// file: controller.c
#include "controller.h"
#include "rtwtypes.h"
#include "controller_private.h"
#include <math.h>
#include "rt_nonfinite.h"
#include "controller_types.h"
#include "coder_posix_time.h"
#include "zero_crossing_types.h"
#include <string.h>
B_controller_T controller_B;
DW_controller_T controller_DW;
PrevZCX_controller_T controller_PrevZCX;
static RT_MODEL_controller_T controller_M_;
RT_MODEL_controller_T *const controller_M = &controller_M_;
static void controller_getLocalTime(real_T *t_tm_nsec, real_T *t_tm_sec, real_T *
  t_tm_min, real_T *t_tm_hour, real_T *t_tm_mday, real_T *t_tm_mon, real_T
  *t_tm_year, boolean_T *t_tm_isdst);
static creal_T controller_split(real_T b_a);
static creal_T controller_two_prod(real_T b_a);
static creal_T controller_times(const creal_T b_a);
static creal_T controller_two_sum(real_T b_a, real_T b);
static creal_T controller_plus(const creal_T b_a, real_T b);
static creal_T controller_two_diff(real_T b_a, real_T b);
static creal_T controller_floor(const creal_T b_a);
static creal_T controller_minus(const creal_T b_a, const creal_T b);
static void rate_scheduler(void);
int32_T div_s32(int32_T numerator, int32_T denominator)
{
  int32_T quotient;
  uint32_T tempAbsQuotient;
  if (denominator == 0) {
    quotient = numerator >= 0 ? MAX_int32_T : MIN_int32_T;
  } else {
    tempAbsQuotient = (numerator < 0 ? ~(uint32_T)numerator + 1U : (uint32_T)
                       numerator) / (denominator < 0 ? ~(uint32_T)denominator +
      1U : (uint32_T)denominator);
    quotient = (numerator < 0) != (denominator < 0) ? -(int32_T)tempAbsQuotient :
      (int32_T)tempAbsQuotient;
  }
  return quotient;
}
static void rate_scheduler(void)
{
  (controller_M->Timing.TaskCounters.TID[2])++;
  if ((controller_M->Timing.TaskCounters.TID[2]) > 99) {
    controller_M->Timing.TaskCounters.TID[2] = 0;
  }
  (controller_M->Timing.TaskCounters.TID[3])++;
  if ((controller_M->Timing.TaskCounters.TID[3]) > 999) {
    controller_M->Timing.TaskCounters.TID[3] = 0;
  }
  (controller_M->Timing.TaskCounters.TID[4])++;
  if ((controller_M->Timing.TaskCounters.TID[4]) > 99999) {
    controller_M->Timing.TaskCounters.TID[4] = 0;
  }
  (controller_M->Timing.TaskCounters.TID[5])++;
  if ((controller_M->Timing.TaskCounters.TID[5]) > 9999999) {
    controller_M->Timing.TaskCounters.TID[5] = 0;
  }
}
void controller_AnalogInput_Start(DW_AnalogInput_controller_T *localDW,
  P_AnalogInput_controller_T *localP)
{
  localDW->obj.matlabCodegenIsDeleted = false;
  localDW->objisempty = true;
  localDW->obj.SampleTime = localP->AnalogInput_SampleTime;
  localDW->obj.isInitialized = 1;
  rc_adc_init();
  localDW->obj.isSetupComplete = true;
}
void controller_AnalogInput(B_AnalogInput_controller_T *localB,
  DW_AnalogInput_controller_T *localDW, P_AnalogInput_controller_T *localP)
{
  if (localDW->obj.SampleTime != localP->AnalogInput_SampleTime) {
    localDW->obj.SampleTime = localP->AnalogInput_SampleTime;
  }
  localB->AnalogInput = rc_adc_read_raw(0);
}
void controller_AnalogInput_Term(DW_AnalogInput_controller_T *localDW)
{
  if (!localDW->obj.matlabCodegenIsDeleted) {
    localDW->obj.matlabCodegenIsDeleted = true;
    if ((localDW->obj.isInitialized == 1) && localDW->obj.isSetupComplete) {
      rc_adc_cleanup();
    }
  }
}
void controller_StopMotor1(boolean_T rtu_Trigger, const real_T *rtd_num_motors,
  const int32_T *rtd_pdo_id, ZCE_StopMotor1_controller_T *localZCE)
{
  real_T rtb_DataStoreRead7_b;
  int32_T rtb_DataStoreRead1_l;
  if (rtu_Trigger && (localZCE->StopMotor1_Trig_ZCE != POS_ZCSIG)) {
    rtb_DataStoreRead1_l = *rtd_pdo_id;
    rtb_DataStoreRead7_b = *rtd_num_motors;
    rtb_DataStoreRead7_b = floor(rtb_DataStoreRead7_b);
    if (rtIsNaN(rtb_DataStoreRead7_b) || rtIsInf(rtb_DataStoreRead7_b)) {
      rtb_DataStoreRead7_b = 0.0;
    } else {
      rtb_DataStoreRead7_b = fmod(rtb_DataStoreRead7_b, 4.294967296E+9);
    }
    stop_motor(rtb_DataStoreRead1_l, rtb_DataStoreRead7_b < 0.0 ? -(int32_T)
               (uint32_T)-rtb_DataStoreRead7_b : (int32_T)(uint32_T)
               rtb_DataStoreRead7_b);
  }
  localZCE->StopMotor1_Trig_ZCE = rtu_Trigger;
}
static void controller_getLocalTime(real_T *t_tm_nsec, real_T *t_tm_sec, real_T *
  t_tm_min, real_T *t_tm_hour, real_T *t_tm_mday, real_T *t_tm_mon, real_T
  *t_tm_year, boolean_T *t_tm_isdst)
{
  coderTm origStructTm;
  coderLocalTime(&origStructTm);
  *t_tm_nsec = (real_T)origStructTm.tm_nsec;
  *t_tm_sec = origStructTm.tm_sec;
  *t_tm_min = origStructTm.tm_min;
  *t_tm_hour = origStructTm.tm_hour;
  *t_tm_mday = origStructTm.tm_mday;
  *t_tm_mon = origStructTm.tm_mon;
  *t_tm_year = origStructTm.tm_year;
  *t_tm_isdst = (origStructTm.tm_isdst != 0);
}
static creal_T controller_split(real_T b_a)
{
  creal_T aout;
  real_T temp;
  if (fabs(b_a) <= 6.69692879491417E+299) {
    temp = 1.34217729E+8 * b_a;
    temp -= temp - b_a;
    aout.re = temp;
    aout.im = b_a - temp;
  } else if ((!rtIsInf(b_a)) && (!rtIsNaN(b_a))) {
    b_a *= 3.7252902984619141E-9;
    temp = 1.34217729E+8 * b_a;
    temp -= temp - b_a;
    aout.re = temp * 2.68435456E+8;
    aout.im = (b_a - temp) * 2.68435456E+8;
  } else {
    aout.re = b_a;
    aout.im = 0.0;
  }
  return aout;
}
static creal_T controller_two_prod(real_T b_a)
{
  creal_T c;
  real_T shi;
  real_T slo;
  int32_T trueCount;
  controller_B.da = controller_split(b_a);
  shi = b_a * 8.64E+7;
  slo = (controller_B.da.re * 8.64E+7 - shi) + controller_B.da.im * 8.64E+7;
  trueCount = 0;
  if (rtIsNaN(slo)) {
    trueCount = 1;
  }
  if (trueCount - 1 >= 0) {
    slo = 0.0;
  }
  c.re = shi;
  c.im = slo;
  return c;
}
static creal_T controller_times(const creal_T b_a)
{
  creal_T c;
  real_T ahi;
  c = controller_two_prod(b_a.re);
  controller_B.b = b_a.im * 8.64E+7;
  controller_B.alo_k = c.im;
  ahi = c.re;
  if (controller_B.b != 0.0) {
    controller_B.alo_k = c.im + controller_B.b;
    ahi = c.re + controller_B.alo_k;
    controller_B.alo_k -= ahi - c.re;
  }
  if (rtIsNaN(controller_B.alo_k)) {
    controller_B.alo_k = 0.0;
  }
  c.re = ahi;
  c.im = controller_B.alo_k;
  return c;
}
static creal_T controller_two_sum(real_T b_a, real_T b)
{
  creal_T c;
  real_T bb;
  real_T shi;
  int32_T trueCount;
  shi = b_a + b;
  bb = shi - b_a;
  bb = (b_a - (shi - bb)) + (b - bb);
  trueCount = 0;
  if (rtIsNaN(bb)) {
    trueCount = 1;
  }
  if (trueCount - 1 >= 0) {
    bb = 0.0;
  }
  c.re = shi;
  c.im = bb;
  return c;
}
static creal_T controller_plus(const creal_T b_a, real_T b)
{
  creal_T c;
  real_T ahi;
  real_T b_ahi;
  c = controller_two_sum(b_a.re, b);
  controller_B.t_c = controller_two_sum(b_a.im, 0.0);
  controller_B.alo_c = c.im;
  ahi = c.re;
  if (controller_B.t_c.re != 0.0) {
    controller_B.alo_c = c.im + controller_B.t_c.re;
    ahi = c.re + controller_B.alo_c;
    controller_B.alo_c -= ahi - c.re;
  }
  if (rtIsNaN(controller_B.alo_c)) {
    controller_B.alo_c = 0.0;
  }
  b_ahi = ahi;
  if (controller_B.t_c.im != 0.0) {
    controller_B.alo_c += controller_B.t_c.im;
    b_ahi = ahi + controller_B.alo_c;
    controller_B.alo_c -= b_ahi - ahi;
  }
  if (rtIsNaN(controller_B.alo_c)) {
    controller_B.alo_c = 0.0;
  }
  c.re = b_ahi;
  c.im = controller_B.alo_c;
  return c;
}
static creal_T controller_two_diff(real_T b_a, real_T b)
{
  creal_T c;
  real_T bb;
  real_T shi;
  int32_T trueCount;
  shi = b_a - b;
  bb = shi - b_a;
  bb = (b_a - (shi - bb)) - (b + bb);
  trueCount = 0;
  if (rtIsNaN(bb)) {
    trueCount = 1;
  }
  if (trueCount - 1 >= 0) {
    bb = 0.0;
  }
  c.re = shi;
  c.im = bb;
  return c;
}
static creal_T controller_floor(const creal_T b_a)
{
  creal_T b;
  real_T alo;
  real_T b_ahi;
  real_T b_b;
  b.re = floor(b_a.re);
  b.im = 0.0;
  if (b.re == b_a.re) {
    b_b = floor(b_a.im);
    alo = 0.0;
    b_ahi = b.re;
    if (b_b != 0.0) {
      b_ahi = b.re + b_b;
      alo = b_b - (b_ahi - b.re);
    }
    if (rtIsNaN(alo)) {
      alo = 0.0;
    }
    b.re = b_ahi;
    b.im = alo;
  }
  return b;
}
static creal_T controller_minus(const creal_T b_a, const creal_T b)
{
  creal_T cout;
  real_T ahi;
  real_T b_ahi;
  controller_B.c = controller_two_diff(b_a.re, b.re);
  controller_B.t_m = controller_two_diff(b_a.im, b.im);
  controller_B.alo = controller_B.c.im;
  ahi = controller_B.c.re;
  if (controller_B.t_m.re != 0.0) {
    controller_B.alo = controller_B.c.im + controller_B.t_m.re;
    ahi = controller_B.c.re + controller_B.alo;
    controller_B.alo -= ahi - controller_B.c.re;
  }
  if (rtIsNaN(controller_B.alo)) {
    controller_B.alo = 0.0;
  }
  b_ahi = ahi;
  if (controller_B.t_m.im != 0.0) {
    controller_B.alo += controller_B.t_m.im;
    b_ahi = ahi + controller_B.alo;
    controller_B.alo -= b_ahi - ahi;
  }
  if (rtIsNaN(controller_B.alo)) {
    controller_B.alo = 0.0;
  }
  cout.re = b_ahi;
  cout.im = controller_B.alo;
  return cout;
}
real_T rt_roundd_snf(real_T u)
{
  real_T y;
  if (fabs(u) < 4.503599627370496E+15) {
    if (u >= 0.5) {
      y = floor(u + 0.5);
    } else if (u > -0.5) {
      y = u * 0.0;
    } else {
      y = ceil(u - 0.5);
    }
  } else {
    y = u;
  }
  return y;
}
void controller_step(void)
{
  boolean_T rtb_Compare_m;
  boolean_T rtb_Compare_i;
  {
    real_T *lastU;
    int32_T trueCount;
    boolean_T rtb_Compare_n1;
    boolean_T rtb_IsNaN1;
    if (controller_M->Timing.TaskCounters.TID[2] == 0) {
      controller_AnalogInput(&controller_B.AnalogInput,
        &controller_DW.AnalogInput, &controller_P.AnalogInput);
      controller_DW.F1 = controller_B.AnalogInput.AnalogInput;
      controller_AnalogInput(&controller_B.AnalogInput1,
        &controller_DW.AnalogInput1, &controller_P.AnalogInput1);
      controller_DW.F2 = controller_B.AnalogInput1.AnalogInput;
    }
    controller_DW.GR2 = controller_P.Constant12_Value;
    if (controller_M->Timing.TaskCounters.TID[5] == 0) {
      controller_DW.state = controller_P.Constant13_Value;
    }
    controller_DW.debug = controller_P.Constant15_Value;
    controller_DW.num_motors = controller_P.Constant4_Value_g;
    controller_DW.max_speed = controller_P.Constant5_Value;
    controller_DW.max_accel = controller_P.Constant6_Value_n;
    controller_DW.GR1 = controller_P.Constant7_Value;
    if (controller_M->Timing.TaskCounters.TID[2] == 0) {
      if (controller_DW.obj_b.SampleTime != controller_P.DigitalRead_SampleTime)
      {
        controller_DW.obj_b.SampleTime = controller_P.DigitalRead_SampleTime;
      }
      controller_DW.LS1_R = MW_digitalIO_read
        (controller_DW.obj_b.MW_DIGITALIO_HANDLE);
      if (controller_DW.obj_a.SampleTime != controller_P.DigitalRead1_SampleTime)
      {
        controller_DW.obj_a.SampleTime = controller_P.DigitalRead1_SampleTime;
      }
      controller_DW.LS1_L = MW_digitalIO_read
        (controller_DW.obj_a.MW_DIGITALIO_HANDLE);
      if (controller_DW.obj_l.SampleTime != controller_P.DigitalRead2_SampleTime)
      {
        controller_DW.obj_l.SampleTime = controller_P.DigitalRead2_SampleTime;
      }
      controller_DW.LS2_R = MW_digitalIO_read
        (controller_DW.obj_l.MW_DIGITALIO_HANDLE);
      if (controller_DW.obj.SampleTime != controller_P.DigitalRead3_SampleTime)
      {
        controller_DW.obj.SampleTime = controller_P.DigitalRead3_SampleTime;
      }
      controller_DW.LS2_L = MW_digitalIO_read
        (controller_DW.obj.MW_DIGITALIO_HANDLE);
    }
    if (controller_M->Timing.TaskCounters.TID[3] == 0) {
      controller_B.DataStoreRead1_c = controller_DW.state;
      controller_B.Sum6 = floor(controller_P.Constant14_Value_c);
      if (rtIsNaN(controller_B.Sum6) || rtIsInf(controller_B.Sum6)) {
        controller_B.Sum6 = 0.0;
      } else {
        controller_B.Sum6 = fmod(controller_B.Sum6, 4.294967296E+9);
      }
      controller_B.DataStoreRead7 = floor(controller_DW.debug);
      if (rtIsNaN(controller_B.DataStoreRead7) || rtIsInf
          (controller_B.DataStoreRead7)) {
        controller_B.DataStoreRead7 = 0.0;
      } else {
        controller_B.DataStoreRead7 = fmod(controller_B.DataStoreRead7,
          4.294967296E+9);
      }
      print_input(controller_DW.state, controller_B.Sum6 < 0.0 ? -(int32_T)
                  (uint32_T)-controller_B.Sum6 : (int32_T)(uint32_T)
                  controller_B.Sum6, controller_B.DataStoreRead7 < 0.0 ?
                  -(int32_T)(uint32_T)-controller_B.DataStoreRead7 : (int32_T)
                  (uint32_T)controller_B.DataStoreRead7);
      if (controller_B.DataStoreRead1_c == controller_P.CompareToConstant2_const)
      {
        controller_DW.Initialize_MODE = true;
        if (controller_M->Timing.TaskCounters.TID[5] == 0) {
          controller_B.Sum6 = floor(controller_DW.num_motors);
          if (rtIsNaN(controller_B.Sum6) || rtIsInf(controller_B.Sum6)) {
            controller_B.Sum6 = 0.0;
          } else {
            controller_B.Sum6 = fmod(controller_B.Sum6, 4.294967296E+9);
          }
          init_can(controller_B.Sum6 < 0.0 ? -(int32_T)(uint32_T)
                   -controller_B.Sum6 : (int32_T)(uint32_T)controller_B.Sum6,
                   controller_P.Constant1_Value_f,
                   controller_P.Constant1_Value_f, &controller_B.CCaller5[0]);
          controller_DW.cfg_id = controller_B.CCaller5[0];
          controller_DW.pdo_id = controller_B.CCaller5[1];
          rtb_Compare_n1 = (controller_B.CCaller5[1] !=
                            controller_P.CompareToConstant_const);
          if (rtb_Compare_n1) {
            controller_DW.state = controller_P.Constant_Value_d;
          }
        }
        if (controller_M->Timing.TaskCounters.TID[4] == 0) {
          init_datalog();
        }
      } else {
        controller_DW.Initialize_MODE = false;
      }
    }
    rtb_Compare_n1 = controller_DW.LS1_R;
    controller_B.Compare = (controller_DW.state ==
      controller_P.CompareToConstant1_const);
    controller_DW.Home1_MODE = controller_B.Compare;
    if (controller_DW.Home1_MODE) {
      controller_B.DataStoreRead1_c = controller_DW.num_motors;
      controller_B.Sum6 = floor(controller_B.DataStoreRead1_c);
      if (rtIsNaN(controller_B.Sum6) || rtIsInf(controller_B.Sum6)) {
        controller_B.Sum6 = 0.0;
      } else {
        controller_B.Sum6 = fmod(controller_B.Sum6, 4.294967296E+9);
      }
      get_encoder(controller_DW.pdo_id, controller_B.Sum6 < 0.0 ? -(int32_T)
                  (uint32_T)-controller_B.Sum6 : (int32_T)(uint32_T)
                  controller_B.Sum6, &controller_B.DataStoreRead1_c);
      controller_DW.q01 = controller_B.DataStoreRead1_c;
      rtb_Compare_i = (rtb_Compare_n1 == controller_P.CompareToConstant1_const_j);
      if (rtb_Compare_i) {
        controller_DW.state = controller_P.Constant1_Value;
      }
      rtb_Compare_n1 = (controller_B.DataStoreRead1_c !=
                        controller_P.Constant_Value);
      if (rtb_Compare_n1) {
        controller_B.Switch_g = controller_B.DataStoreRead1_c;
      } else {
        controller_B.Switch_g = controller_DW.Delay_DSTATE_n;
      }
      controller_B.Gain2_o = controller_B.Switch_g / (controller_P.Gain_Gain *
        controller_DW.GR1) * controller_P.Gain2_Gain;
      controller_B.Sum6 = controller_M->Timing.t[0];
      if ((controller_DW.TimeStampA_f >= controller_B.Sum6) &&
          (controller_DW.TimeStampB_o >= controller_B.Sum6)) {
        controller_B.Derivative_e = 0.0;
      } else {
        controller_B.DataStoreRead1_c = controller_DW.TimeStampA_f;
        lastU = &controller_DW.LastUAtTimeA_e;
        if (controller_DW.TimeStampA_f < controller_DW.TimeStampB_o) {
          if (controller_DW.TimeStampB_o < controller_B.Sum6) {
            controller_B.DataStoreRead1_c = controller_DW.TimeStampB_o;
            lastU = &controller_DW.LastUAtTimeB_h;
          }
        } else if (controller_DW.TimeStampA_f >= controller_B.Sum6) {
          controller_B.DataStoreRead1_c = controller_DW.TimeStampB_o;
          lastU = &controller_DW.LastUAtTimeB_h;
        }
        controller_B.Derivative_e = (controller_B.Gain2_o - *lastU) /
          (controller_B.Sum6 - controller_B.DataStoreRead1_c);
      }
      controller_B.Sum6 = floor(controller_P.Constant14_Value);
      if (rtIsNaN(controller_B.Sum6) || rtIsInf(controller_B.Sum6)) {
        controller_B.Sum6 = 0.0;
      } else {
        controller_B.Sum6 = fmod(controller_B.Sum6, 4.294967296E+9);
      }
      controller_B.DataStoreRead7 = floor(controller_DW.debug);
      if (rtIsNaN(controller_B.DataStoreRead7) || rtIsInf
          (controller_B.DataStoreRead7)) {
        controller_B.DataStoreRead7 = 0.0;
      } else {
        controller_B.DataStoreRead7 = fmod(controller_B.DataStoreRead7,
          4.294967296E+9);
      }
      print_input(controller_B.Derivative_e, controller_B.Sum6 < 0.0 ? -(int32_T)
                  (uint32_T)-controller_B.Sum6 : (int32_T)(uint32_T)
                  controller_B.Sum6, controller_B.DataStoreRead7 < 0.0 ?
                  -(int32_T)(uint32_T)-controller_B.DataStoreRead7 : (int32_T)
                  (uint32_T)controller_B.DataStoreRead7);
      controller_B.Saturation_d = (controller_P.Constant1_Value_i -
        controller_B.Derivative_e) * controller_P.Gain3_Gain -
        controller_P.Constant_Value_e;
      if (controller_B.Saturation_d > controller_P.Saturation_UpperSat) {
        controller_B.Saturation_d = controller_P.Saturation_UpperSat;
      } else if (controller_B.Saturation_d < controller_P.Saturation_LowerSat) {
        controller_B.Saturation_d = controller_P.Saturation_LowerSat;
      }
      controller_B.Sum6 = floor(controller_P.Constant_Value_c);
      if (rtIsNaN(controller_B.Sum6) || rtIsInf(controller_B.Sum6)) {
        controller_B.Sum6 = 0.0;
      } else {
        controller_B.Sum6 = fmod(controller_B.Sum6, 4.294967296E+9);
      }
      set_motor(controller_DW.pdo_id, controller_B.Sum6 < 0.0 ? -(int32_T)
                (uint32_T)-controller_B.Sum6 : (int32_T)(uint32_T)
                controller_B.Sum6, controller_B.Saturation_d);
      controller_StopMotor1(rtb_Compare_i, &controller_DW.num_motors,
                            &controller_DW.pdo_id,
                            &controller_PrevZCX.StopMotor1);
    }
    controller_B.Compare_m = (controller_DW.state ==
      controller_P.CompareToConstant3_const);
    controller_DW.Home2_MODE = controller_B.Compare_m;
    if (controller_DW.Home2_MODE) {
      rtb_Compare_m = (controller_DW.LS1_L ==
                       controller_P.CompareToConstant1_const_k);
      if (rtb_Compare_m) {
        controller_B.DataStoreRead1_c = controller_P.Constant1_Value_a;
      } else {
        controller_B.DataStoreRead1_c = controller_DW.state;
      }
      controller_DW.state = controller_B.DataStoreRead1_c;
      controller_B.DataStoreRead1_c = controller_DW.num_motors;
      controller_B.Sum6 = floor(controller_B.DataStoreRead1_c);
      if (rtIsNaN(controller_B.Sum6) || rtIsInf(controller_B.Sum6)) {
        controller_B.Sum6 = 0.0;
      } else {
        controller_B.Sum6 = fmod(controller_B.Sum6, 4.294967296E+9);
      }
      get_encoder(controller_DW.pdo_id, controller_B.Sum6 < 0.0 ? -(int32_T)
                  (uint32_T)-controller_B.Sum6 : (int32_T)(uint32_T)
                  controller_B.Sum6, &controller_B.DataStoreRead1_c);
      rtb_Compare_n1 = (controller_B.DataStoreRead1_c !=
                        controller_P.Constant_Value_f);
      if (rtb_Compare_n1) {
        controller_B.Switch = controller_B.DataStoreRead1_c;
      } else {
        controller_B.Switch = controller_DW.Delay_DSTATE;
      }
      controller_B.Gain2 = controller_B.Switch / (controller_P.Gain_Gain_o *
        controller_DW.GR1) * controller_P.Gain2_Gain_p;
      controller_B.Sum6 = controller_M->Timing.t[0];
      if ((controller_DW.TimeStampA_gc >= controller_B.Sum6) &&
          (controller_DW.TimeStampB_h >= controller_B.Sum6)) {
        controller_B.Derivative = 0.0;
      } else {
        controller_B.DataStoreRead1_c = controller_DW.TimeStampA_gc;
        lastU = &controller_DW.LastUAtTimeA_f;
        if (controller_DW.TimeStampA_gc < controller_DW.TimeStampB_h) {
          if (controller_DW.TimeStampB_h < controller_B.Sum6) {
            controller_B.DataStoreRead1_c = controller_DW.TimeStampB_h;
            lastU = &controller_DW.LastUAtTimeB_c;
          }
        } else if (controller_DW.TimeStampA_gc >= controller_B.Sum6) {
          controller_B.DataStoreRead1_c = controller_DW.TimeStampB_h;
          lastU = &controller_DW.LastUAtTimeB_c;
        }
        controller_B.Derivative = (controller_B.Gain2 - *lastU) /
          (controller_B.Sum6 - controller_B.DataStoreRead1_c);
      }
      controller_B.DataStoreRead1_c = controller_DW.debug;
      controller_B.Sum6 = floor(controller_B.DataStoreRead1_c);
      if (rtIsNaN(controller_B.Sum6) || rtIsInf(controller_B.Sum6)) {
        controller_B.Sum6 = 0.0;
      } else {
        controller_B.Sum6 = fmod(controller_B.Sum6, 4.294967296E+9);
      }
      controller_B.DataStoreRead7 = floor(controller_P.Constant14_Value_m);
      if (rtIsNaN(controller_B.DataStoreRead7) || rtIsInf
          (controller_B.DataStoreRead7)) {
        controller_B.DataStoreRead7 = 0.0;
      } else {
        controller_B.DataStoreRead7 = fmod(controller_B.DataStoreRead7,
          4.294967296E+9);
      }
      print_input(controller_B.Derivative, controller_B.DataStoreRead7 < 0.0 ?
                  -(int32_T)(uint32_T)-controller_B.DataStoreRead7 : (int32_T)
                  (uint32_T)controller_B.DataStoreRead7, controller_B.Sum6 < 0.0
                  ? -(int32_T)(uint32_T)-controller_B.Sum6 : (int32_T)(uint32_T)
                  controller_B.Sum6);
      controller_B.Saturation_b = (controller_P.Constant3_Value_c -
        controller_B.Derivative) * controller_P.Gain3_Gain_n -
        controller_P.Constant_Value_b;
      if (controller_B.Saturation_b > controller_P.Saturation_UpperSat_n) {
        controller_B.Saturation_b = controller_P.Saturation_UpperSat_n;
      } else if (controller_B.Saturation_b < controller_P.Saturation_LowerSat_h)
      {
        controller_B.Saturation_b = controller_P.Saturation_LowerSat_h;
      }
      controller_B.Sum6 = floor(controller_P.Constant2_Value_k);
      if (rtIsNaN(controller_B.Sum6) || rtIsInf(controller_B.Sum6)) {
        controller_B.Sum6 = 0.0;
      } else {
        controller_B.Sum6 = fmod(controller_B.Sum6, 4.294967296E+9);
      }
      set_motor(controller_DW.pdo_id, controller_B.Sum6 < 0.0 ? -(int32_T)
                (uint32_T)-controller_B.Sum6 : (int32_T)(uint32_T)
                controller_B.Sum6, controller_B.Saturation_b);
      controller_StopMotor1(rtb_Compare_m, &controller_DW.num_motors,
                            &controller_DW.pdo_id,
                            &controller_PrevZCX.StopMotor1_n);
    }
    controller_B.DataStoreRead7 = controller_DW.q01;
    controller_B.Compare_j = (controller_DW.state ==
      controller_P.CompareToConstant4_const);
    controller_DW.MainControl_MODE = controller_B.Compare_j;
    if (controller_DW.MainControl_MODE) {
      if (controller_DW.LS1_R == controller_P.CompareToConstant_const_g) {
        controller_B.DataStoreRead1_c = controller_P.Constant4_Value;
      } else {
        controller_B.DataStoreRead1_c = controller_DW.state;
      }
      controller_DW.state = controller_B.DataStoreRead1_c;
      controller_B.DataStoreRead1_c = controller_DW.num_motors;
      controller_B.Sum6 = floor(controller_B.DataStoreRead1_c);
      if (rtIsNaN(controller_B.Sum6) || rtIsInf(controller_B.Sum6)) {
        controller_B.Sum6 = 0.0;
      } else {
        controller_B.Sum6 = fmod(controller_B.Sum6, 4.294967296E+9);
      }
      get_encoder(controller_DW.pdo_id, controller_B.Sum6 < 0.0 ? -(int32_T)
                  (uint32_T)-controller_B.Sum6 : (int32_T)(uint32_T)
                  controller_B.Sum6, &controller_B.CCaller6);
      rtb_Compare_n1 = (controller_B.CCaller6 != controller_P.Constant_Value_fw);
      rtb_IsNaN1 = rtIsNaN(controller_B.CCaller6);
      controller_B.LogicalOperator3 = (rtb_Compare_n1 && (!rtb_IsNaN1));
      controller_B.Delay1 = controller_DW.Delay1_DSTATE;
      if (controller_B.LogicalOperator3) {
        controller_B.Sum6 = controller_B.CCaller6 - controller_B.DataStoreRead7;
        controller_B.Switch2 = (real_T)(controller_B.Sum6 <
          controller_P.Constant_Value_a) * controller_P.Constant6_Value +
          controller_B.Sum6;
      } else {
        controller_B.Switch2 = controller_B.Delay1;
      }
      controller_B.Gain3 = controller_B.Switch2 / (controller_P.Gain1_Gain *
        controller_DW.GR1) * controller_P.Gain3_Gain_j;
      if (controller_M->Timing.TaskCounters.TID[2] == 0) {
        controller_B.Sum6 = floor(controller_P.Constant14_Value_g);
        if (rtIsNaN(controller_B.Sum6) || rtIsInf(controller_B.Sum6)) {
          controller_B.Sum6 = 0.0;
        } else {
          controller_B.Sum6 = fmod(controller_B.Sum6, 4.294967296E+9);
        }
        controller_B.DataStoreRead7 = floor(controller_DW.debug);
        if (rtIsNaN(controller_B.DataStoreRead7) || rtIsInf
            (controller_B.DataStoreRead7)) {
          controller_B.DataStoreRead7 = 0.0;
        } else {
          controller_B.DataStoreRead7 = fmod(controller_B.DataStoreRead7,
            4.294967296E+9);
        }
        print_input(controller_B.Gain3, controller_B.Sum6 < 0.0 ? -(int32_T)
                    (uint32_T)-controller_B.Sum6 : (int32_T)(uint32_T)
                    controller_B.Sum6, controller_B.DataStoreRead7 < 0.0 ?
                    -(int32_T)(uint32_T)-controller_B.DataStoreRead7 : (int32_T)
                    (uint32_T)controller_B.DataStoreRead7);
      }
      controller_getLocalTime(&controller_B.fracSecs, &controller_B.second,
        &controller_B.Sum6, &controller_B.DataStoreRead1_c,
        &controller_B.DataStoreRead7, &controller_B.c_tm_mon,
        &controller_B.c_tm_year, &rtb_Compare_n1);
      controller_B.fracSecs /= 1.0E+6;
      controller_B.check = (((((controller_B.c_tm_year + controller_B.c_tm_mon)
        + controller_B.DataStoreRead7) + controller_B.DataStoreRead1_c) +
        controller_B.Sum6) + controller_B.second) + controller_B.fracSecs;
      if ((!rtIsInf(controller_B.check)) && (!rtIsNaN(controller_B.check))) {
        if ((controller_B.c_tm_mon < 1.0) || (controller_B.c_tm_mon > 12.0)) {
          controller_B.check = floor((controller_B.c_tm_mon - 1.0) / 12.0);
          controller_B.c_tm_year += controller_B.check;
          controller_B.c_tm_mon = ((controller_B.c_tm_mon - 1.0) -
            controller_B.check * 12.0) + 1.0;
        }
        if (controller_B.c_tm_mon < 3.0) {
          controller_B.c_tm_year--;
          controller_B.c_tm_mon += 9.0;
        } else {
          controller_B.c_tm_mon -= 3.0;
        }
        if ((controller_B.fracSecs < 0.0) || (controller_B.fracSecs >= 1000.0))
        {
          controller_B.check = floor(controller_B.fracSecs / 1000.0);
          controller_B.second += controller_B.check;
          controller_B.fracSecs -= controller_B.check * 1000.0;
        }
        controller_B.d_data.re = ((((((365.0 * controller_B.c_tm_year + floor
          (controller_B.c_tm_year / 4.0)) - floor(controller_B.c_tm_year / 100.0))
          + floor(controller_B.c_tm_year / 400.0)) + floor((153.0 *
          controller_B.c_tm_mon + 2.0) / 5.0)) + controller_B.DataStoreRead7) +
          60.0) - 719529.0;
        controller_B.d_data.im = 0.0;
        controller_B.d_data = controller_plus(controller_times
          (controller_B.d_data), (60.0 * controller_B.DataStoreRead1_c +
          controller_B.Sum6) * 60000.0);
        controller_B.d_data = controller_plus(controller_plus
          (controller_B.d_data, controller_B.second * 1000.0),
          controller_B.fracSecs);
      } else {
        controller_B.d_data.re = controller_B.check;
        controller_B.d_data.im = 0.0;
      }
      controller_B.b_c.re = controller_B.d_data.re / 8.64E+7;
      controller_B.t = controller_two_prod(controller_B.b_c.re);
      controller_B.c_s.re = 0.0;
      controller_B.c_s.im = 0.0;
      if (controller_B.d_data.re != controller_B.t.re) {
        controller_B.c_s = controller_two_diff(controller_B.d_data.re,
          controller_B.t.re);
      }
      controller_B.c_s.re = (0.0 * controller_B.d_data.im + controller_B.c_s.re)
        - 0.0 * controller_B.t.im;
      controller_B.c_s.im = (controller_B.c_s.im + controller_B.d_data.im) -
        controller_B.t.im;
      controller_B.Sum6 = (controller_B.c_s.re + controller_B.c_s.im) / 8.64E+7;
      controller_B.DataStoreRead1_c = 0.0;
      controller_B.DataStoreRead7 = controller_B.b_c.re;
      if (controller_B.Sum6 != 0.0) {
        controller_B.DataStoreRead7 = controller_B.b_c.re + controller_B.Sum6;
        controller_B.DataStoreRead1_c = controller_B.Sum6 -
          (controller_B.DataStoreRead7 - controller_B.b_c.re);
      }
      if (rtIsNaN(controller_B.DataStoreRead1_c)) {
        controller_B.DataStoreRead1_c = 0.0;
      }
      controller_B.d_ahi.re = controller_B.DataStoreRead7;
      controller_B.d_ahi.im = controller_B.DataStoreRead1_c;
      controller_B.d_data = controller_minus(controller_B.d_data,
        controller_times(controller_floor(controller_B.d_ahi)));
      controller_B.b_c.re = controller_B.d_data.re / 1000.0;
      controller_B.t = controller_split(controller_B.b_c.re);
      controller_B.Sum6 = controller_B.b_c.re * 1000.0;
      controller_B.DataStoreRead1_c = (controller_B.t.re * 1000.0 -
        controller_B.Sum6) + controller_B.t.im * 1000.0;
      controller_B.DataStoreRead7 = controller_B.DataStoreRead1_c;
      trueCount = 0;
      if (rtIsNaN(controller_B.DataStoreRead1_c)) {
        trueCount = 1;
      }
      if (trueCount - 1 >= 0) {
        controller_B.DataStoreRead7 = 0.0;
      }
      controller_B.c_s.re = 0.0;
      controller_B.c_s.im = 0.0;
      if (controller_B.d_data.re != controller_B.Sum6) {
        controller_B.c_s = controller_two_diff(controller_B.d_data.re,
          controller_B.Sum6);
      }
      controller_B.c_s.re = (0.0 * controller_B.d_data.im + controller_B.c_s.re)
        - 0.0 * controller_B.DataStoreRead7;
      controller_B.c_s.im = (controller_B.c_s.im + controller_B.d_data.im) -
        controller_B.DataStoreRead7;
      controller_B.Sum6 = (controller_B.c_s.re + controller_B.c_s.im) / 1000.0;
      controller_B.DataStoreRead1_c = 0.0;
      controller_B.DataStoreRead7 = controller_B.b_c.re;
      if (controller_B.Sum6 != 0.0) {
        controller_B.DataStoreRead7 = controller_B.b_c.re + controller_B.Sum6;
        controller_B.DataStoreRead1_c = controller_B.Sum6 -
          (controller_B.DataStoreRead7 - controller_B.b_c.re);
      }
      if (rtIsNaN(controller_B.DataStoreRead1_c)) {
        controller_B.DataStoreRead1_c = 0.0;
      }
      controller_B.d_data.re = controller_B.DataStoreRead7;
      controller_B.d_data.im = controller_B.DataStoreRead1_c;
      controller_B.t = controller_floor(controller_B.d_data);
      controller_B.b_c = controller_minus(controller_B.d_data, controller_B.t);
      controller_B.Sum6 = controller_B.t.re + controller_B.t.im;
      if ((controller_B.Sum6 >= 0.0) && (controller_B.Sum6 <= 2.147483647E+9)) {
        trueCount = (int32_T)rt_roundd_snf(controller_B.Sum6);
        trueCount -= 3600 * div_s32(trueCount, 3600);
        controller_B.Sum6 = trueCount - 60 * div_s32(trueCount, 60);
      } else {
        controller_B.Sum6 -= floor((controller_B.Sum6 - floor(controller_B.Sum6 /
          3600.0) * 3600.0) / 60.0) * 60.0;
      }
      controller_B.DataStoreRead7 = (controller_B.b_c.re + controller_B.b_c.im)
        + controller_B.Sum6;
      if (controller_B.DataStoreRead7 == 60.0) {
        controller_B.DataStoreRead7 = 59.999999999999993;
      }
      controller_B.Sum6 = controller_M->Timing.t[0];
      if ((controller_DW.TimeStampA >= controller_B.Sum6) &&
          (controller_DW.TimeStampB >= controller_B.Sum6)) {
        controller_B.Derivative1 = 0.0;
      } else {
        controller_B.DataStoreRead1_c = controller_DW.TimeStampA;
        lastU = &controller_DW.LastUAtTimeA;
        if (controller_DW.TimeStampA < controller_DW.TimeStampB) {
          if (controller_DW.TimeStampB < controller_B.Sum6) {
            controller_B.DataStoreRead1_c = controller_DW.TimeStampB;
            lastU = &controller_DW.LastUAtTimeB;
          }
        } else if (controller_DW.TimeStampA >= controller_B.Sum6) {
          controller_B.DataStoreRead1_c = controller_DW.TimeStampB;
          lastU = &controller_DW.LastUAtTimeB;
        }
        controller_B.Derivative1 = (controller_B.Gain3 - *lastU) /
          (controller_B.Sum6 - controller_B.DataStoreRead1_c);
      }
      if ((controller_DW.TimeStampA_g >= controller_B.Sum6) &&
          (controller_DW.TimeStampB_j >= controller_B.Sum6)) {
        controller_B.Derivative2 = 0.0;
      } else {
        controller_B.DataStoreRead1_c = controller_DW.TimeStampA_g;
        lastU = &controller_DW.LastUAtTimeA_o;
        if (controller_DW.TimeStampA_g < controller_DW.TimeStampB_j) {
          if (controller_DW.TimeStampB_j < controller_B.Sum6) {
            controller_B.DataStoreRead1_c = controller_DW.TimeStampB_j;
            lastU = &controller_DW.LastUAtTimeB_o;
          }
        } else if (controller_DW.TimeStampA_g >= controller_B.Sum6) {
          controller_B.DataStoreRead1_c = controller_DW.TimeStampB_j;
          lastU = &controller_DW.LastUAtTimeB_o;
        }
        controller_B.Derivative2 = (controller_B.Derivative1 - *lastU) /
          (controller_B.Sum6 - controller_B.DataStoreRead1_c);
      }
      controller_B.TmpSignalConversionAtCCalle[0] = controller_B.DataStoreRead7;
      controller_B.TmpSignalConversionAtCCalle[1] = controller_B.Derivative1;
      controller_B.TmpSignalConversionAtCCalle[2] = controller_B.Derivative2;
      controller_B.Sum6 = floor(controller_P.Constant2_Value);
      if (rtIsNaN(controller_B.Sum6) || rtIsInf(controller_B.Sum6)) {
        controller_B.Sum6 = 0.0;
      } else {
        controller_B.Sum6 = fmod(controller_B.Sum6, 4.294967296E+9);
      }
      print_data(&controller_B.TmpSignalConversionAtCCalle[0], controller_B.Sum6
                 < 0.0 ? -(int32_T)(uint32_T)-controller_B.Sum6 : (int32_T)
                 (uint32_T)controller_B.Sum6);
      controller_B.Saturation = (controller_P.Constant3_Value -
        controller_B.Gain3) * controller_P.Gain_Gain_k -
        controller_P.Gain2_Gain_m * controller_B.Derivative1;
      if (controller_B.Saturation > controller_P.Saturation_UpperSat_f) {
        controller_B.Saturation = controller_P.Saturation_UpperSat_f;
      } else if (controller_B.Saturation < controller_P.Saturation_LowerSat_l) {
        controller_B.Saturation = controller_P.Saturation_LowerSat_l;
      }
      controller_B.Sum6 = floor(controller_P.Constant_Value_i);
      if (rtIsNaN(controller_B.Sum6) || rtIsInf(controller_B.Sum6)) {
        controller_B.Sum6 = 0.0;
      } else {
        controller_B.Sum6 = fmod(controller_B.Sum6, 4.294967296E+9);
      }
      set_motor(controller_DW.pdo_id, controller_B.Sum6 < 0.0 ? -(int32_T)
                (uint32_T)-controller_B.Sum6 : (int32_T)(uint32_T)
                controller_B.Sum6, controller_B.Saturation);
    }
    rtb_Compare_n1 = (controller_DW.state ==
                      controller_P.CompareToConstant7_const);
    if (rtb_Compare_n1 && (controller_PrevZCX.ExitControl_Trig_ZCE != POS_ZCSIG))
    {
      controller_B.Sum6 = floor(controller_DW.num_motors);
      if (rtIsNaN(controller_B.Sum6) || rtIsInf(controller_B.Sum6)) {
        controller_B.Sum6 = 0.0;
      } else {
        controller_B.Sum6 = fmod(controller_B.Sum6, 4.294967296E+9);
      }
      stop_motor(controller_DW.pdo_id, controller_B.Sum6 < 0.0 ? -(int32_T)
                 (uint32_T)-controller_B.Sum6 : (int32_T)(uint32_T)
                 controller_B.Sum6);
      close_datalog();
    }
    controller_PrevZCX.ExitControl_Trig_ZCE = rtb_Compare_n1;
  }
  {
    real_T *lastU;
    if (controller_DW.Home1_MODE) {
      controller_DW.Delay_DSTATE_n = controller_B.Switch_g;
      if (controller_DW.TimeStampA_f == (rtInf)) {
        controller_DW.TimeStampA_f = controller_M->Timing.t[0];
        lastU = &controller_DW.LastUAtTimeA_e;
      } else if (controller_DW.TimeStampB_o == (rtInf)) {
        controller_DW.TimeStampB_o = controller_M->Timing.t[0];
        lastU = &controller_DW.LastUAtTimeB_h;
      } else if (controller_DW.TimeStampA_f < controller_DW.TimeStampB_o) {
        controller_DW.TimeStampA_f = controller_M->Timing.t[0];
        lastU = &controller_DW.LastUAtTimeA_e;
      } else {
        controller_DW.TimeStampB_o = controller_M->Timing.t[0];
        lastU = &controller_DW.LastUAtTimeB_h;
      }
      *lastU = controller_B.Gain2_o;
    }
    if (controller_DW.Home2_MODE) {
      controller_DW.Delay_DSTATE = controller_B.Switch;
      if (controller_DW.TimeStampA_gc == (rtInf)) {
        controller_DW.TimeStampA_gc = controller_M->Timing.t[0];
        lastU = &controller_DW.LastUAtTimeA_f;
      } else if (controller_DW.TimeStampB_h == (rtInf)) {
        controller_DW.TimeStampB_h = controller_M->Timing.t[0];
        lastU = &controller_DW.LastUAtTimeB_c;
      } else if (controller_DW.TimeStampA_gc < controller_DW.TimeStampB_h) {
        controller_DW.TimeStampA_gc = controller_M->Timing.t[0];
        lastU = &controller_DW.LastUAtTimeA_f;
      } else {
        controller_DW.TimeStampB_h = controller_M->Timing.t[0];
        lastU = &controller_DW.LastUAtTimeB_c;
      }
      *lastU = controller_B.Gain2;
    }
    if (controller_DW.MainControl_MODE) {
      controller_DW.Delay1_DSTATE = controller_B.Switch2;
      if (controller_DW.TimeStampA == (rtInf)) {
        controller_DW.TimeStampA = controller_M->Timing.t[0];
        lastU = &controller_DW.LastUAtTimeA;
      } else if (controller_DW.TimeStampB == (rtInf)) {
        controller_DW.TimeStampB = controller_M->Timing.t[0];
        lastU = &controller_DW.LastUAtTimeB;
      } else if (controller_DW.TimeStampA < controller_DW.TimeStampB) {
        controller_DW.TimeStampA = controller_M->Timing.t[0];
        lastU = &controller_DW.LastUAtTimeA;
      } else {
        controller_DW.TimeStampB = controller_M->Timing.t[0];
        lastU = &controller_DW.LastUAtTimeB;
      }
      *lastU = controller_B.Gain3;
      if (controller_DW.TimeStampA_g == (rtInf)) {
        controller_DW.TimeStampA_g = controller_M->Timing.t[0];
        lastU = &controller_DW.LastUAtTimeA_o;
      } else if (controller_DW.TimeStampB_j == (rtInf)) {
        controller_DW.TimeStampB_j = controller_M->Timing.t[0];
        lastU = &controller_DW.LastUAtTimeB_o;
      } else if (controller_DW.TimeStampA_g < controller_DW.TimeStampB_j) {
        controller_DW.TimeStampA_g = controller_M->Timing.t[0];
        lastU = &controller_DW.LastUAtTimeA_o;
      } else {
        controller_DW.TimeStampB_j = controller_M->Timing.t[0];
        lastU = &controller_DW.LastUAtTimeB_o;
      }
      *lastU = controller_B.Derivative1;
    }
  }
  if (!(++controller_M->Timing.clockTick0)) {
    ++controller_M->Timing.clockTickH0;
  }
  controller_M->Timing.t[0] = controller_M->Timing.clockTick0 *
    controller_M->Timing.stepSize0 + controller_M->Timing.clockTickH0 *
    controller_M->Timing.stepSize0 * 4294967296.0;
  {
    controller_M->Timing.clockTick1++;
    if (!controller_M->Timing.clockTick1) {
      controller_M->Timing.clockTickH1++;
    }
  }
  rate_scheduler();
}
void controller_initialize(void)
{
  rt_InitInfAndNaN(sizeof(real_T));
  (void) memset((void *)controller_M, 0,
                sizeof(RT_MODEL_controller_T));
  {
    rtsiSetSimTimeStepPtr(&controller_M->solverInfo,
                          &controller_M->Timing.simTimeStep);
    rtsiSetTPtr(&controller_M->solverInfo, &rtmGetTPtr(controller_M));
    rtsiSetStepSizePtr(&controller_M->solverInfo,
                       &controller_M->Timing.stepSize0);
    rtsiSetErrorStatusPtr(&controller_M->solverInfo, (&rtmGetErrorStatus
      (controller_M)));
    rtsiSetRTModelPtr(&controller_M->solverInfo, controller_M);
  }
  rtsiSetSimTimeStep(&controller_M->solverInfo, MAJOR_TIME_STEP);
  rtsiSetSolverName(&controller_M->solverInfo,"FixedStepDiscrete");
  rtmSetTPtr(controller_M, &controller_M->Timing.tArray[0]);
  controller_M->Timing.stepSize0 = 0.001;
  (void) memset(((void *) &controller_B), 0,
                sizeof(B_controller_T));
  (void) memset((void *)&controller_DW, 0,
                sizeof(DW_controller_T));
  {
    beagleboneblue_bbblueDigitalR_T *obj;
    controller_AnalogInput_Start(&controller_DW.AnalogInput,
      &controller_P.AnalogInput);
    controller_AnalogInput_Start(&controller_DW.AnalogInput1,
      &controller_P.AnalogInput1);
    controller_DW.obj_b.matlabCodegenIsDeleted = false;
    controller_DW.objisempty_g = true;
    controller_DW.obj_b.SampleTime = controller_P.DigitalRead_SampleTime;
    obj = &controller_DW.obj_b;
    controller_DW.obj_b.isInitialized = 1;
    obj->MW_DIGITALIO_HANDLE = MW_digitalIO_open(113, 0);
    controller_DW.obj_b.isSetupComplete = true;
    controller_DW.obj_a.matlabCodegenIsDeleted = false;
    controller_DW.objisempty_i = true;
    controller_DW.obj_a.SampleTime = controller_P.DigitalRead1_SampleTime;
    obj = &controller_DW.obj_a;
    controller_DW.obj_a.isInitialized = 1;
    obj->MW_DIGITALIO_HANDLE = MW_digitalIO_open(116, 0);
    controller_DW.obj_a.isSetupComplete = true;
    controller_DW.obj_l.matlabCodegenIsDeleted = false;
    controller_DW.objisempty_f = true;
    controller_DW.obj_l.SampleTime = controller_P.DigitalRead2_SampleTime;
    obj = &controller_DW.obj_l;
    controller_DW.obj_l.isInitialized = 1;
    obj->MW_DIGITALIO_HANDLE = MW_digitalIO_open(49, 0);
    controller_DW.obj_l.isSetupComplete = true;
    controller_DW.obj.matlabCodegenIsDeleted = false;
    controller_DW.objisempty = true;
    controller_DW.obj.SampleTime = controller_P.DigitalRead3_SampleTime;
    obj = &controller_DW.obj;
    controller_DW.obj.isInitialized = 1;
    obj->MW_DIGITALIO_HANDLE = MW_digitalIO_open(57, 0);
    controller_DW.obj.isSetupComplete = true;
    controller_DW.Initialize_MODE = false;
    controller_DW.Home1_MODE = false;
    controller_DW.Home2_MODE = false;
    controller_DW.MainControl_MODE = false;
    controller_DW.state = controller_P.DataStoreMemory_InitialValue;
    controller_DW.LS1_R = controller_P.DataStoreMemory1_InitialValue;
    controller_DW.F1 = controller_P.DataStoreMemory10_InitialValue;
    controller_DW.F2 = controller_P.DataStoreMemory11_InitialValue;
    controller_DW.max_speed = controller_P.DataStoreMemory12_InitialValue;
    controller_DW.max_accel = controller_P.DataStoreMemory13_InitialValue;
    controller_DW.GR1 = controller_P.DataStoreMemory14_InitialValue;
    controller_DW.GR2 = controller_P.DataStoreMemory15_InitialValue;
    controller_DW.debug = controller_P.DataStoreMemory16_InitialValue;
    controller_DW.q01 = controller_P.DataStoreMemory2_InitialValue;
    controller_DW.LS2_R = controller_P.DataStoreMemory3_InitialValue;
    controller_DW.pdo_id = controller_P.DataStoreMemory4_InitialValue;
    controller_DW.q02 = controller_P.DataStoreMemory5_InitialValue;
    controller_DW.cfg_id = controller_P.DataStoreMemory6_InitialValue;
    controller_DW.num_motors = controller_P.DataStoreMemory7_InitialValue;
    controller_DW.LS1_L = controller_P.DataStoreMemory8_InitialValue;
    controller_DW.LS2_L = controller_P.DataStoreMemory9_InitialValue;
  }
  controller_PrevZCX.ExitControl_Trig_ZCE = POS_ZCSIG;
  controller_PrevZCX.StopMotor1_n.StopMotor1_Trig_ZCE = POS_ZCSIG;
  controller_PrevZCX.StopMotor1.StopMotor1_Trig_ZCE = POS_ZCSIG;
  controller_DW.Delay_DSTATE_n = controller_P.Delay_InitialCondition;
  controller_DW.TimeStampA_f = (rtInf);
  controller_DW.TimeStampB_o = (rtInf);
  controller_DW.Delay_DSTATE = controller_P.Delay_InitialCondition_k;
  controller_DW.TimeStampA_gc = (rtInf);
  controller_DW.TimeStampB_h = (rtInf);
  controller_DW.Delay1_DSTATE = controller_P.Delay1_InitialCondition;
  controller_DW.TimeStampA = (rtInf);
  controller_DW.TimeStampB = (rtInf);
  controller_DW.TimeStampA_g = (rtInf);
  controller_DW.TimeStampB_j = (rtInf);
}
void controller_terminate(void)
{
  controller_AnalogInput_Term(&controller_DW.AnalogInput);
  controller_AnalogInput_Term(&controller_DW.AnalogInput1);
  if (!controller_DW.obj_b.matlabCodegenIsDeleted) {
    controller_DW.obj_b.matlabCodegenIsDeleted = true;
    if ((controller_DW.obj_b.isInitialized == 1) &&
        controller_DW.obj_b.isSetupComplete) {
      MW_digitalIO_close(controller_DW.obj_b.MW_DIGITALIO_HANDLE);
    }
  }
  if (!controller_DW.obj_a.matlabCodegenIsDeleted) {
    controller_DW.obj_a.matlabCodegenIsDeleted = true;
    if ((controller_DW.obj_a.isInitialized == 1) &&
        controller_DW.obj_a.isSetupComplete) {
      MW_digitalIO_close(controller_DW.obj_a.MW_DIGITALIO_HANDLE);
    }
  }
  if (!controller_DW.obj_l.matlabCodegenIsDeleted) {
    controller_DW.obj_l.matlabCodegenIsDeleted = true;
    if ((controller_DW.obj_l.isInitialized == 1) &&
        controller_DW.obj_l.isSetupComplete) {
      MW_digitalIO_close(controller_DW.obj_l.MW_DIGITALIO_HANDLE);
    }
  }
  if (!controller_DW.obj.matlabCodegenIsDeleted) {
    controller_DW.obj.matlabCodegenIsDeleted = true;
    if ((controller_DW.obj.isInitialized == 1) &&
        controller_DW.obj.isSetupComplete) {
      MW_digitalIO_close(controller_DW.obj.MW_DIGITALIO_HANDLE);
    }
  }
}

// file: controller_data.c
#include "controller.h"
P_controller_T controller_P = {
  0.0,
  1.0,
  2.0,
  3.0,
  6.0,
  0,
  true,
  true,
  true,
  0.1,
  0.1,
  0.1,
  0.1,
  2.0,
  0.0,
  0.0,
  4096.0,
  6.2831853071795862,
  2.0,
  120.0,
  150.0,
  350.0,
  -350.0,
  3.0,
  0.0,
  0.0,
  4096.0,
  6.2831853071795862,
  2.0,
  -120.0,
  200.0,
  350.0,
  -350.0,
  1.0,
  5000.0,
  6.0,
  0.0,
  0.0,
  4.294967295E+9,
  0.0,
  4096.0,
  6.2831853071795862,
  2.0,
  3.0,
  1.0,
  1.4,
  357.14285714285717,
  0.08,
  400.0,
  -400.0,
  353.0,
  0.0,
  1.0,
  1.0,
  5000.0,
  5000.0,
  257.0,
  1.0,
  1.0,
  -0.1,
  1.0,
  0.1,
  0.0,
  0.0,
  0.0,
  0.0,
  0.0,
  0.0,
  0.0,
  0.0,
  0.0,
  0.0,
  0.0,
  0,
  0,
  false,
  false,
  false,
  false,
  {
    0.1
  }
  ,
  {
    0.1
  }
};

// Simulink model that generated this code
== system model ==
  DataStoreWrite#1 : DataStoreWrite  DataStoreName=F1  Indices=1  <- 1: AnalogInput
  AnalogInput : bbblueBasicLib/Analog Input
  DataStoreWrite#2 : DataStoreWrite  DataStoreName=F2  Indices=1  <- 1: AnalogInput1
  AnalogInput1 : bbblueBasicLib/Analog Input
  DataStoreWrite#3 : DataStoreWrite  DataStoreName=GR2  Indices=1  <- 1: Constant12
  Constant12 : Constant  Value=353
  DataStoreWrite#4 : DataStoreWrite  DataStoreName=state  Indices=1  <- 1: Constant13
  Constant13 : Constant  Value=0
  DataStoreWrite#5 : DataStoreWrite  DataStoreName=debug  Indices=1  <- 1: Constant15
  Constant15 : Constant
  DataStoreWrite#6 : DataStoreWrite  DataStoreName=num_motors  Indices=1  <- 1: Constant4
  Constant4 : Constant
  DataStoreWrite#7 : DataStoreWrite  DataStoreName=max_speed  Indices=1  <- 1: Constant5
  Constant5 : Constant  Value=5000
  DataStoreWrite#8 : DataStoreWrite  DataStoreName=max_accel  Indices=1  <- 1: Constant6
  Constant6 : Constant  Value=5000
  DataStoreWrite#9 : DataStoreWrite  DataStoreName=GR1  Indices=1  <- 1: Constant7
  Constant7 : Constant  Value=257
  DataStoreWrite#10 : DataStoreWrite  DataStoreName=LS1_R  Indices=1  <- 1: DigitalRead
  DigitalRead : bbblueBasicLib/Digital Read
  DataStoreWrite#11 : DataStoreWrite  DataStoreName=LS1_L  Indices=1  <- 1: DigitalRead1
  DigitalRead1 : bbblueBasicLib/Digital Read
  DataStoreWrite#12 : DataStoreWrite  DataStoreName=LS2_R  Indices=1  <- 1: DigitalRead2
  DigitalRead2 : bbblueBasicLib/Digital Read
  DataStoreWrite#13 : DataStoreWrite  DataStoreName=LS2_L  Indices=1  <- 1: DigitalRead3
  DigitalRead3 : bbblueBasicLib/Digital Read
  CCaller#1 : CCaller  FunctionName=print_input  <- 1: DataTypeConversion#1, 2: DataTypeConversion#2, 3: DataTypeConversion#3
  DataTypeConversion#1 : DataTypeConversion  <- 1: DataStoreRead1
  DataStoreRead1 : DataStoreRead  DataStoreName=state  Indices=1
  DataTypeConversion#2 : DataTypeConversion  <- 1: Constant14
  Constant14 : Constant
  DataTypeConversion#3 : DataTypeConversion  <- 1: DataStoreRead#1
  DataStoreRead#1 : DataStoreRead  DataStoreName=debug  Indices=1
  Initialize : Subsystem  <- Enable: CompareToConstant2
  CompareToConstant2 : simulink/Logic and Bit Operations/Compare To Constant  relop===  const=0  <- 1: DataStoreRead1
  Home1 : Subsystem  <- 1: Constant, 2: Constant1, 3: DataStoreRead#2, Enable: CompareToConstant1
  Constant : Constant
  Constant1 : Constant  Value=-0.1
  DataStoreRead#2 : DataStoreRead  DataStoreName=LS1_R  Indices=1
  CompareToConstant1 : simulink/Logic and Bit Operations/Compare To Constant  relop===  const=1  <- 1: DataStoreRead#3
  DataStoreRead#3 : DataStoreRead  DataStoreName=state  Indices=1
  Home2 : Subsystem  <- 1: Constant2, 2: Constant3, 3: DataStoreRead#4, Enable: CompareToConstant3
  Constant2 : Constant
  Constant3 : Constant  Value=0.1
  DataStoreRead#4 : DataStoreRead  DataStoreName=LS1_L  Indices=1
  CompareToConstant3 : simulink/Logic and Bit Operations/Compare To Constant  relop===  const=2  <- 1: DataStoreRead#5
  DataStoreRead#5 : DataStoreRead  DataStoreName=state  Indices=1
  MainControl : Subsystem  <- 1: DataStoreRead7, Enable: CompareToConstant4
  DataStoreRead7 : DataStoreRead  DataStoreName=q01  Indices=1
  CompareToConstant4 : simulink/Logic and Bit Operations/Compare To Constant  relop===  const=3  <- 1: DataStoreRead#6
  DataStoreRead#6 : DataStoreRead  DataStoreName=state  Indices=1
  DataStoreRead#7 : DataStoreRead  DataStoreName=q02  Indices=1
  ExitControl : Subsystem  <- Trigger: CompareToConstant7
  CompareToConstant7 : simulink/Logic and Bit Operations/Compare To Constant  relop===  const=6  <- 1: DataStoreRead#8
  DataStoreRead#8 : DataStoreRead  DataStoreName=state  Indices=1
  DataStoreMemory : DataStoreMemory  DataStoreName=state
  DataStoreMemory1 : DataStoreMemory  DataStoreName=LS1_R
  DataStoreMemory10 : DataStoreMemory  DataStoreName=F1
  DataStoreMemory11 : DataStoreMemory  DataStoreName=F2
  DataStoreMemory12 : DataStoreMemory  DataStoreName=max_speed
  DataStoreMemory13 : DataStoreMemory  DataStoreName=max_accel
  DataStoreMemory14 : DataStoreMemory  DataStoreName=GR1
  DataStoreMemory15 : DataStoreMemory  DataStoreName=GR2
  DataStoreMemory16 : DataStoreMemory  DataStoreName=debug
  DataStoreMemory2 : DataStoreMemory  DataStoreName=q01
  DataStoreMemory3 : DataStoreMemory  DataStoreName=LS2_R
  DataStoreMemory4 : DataStoreMemory  DataStoreName=pdo_id
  DataStoreMemory5 : DataStoreMemory  DataStoreName=q02
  DataStoreMemory6 : DataStoreMemory  DataStoreName=cfg_id
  DataStoreMemory7 : DataStoreMemory  DataStoreName=num_motors
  DataStoreMemory8 : DataStoreMemory  DataStoreName=LS1_L
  DataStoreMemory9 : DataStoreMemory  DataStoreName=LS2_L
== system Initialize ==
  EnablePort#1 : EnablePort
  DataStoreWrite#14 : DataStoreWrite  DataStoreName=pdo_id  Indices=1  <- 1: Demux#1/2
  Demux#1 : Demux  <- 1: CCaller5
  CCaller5 : CCaller  FunctionName=init_can  <- 1: DataTypeConversion#4, 2: Constant#1, 3: Constant#1
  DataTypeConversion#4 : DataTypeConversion  <- 1: DataStoreRead#9
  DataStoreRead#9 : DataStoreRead  DataStoreName=num_motors  Indices=1
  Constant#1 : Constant  Value=5000
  DataStoreWrite#15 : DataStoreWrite  DataStoreName=cfg_id  Indices=1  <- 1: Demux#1
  DataStoreWrite#16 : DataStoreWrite  DataStoreName=state  Indices=1  <- 1: Switch
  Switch : Switch  Criteria=u2 > Threshold  <- 1: Constant#2, 2: CompareToConstant, 3: DataStoreRead#10
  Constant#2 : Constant
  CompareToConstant : simulink/Logic and Bit Operations/Compare To Constant  relop=~=  const=0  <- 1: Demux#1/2
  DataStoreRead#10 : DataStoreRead  DataStoreName=state  Indices=1
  CCaller#2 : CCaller  FunctionName=init_datalog
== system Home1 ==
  Inport#1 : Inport
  Inport#2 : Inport
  LS1 : Inport
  EnablePort#2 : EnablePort
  StopMotor1 : Subsystem  <- Trigger: CompareToConstant#1
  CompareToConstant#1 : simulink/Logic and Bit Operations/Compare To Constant  relop===  const=1  <- 1: LS1
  DataStoreWrite#17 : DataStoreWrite  DataStoreName=q01  Indices=1  <- 1: CCaller#3
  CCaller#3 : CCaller  FunctionName=get_encoder  <- 1: DataStoreRead#11, 2: DataTypeConversion#5
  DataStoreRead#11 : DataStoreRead  DataStoreName=pdo_id  Indices=1
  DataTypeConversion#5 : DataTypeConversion  <- 1: DataStoreRead#12
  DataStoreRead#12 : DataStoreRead  DataStoreName=num_motors  Indices=1
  DataStoreWrite#18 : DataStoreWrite  DataStoreName=state  Indices=1  <- 1: Switch#1
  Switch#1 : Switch  Criteria=u2 > Threshold  <- 1: Constant#3, 2: CompareToConstant#1, 3: DataStoreRead#13
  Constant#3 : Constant  Value=2
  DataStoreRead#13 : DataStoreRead  DataStoreName=state  Indices=1
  CCaller#4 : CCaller  FunctionName=print_input  <- 1: DataTypeConversion#6, 2: DataTypeConversion#7, 3: DataTypeConversion#8
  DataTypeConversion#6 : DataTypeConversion  <- 1: Derivative
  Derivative : Derivative  <- 1: Gain2
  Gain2 : Gain  Gain=2*pi  <- 1: Product#1
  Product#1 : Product  Inputs=*/  <- 1: Switch#2, 2: Gain
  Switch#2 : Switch  Criteria=u2 > Threshold  <- 1: CCaller#3, 2: CompareToZero#1, 3: Delay
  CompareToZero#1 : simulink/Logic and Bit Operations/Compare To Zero  relop=~=  <- 1: CCaller#3
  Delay : Delay  DelayLength=1  InitialCondition=0  <- 1: Switch#2
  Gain : Gain  Gain=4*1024  <- 1: DataStoreRead#14
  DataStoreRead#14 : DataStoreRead  DataStoreName=GR1  Indices=1
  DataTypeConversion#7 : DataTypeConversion  <- 1: Constant#4
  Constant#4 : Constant  Value=2
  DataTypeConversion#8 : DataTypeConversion  <- 1: DataStoreRead#15
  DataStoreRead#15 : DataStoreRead  DataStoreName=debug  Indices=1
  CCaller#5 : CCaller  FunctionName=set_motor  <- 1: DataTypeConversion#9, 2: DataTypeConversion#10, 3: Saturation
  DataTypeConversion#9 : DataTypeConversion  <- 1: DataStoreRead#16
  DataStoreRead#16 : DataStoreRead  DataStoreName=pdo_id  Indices=1
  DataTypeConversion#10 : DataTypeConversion  <- 1: Inport#1
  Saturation : Saturate  UpperLimit=350  LowerLimit=-350  <- 1: Sum#1
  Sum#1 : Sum  Inputs=-+-  <- 1: Constant#5, 2: Gain3
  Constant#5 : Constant  Value=120
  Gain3 : Gain  Gain=150  <- 1: Sum#2
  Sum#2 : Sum  Inputs=+-  <- 1: Inport#2, 2: Derivative
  Gain1 : Gain  Gain=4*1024  <- 1: DataStoreRead#17
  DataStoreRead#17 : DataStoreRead  DataStoreName=GR2  Indices=1
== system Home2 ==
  Inport#3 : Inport
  Inport#4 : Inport
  Inport#5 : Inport
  EnablePort#3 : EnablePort
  Subsystem#1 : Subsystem  <- Trigger: CompareToConstant#2
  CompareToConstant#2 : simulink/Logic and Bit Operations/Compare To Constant  relop===  const=1  <- 1: Inport#5
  DataStoreWrite#19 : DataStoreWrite  DataStoreName=state  Indices=1  <- 1: Switch#3
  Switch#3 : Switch  Criteria=u2 > Threshold  <- 1: Constant#6, 2: CompareToConstant#2, 3: DataStoreRead#18
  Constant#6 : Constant  Value=3
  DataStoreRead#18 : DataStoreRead  DataStoreName=state  Indices=1
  CCaller#6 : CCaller  FunctionName=print_input  <- 1: DataTypeConversion#11, 2: DataTypeConversion#12, 3: DataTypeConversion#13
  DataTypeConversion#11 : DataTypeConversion  <- 1: Derivative#1
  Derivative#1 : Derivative  <- 1: Gain#1
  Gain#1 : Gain  Gain=2*pi  <- 1: Product#2
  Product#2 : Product  Inputs=*/  <- 1: Switch#4, 2: Gain#2
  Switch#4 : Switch  Criteria=u2 > Threshold  <- 1: CCaller#7, 2: CompareToZero#2, 3: Delay#1
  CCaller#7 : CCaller  FunctionName=get_encoder  <- 1: DataStoreRead#19, 2: DataTypeConversion#14
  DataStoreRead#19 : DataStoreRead  DataStoreName=pdo_id  Indices=1
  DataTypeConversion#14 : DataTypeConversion  <- 1: DataStoreRead#20
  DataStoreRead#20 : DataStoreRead  DataStoreName=num_motors  Indices=1
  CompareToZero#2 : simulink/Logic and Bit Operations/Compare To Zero  relop=~=  <- 1: CCaller#7
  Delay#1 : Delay  DelayLength=1  InitialCondition=0  <- 1: Switch#4
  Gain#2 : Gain  Gain=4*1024  <- 1: DataStoreRead#21
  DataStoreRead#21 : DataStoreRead  DataStoreName=GR1  Indices=1
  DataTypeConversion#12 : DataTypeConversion  <- 1: Constant#7
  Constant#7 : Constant  Value=2
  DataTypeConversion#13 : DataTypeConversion  <- 1: DataStoreRead#22
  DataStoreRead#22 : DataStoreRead  DataStoreName=debug  Indices=1
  CCaller#8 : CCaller  FunctionName=set_motor  <- 1: DataTypeConversion#15, 2: DataTypeConversion#16, 3: Saturate#1
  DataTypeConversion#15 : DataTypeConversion  <- 1: DataStoreRead#23
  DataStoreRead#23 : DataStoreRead  DataStoreName=pdo_id  Indices=1
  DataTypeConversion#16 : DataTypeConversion  <- 1: Inport#3
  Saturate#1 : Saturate  UpperLimit=350  LowerLimit=-350  <- 1: Sum#3
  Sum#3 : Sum  Inputs=-+-  <- 1: Constant#8, 2: Gain#3
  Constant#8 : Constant  Value=-120
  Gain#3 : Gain  Gain=200  <- 1: Sum#4
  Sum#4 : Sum  Inputs=+-  <- 1: Inport#4, 2: Derivative#1
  Gain#4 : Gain  Gain=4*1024  <- 1: DataStoreRead#24
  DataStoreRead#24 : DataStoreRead  DataStoreName=GR2  Indices=1
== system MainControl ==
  Inport#6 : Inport
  EnablePort#4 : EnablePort
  CCaller#9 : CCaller  FunctionName=print_data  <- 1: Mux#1, 2: DataTypeConversion#17
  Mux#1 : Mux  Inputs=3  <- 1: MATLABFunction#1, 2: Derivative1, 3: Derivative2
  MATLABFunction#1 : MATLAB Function
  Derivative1 : Derivative  <- 1: Gain#5
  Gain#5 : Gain  Gain=2*pi  <- 1: Product#3
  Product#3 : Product  Inputs=*/  <- 1: Switch2, 2: Gain#6
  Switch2 : Switch  Criteria=u2 > Threshold  <- 1: Sum#5, 2: LogicalOperator3, 3: Delay1
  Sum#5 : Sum  Inputs=++  <- 1: Product#4, 2: Sum6
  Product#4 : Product  Inputs=**  <- 1: Constant#9, 2: CompareToZero#3
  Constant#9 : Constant  Value=4294967295
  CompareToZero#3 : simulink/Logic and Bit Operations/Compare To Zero  relop=<  <- 1: Sum6
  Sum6 : Sum  Inputs=-+  <- 1: Inport#6, 2: CCaller6
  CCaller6 : CCaller  FunctionName=get_encoder  <- 1: DataStoreRead#25, 2: DataTypeConversion#18
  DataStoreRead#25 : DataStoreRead  DataStoreName=pdo_id  Indices=1
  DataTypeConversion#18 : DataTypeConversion  <- 1: DataStoreRead#26
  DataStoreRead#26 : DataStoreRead  DataStoreName=num_motors  Indices=1
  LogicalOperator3 : Logic  <- 1: CompareToZero#4, 2: Logic#1
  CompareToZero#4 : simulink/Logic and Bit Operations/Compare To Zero  relop=~=  <- 1: CCaller6
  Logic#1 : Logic  Operator=NOT  <- 1: IsNaN1
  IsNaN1 : RelationalOperator  Operator=isNaN  <- 1: CCaller6
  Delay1 : Delay  DelayLength=1  InitialCondition=0  <- 1: Switch2
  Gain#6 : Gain  Gain=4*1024  <- 1: DataStoreRead#27
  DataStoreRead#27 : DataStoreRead  DataStoreName=GR1  Indices=1
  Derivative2 : Derivative  <- 1: Derivative1
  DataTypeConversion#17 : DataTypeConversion  <- 1: Constant#10
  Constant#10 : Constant  Value=3
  DataStoreWrite#20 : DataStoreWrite  DataStoreName=state  Indices=1  <- 1: Switch#5
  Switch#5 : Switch  Criteria=u2 > Threshold  <- 1: Constant#11, 2: CompareToConstant#3, 3: DataStoreRead#28
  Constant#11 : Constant  Value=6
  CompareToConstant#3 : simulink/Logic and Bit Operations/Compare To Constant  relop===  const=1  <- 1: DataStoreRead#29
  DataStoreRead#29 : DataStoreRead  DataStoreName=LS1_R  Indices=1
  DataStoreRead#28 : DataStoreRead  DataStoreName=state  Indices=1
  CCaller#10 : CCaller  FunctionName=print_input  <- 1: DataTypeConversion#19, 2: DataTypeConversion#20, 3: DataTypeConversion#21
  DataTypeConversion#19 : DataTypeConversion  <- 1: Gain#5
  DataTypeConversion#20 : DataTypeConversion  <- 1: Constant#12
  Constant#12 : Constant  Value=2
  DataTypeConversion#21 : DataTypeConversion  <- 1: DataStoreRead#30
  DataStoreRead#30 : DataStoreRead  DataStoreName=debug  Indices=1
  CCaller#11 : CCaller  FunctionName=set_motor  <- 1: DataTypeConversion#22, 2: DataTypeConversion#23, 3: Saturate#2
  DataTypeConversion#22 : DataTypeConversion  <- 1: DataStoreRead#31
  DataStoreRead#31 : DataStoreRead  DataStoreName=pdo_id  Indices=1
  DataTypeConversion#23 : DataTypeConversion  <- 1: Constant#13
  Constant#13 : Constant
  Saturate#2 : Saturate  UpperLimit=400  LowerLimit=-400  <- 1: Sum#6
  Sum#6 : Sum  Inputs=+-  <- 1: Gain#7, 2: Gain#8
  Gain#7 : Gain  Gain=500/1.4  <- 1: Sum#7
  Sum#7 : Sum  Inputs=+-  <- 1: Constant#14, 2: Gain#5
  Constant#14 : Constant  Value=1.4
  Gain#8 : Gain  Gain=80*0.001  <- 1: Derivative1
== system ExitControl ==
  Trigger : TriggerPort
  CCaller#12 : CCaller  FunctionName=close_datalog
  CCaller#13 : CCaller  FunctionName=stop_motor  <- 1: DataStoreRead#32, 2: DataTypeConversion#24
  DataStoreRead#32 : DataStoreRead  DataStoreName=pdo_id  Indices=1
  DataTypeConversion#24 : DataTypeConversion  <- 1: DataStoreRead#33
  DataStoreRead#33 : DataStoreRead  DataStoreName=num_motors  Indices=1
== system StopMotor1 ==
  TriggerPort#1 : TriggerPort
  CCaller#14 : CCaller  FunctionName=stop_motor  <- 1: DataStoreRead#34, 2: DataTypeConversion#25
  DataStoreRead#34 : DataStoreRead  DataStoreName=pdo_id  Indices=1
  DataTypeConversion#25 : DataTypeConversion  <- 1: DataStoreRead#35
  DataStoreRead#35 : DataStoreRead  DataStoreName=num_motors  Indices=1
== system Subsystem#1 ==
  TriggerPort#2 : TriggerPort
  CCaller#15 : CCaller  FunctionName=stop_motor  <- 1: DataStoreRead#36, 2: DataTypeConversion#26
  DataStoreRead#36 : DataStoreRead  DataStoreName=pdo_id  Indices=1
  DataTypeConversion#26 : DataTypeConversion  <- 1: DataStoreRead#37
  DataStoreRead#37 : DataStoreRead  DataStoreName=num_motors  Indices=1
== matlab function MATLABFunction#1 ==
function y = sysTime()
    c = datetime('now')
    y=c.Second;
